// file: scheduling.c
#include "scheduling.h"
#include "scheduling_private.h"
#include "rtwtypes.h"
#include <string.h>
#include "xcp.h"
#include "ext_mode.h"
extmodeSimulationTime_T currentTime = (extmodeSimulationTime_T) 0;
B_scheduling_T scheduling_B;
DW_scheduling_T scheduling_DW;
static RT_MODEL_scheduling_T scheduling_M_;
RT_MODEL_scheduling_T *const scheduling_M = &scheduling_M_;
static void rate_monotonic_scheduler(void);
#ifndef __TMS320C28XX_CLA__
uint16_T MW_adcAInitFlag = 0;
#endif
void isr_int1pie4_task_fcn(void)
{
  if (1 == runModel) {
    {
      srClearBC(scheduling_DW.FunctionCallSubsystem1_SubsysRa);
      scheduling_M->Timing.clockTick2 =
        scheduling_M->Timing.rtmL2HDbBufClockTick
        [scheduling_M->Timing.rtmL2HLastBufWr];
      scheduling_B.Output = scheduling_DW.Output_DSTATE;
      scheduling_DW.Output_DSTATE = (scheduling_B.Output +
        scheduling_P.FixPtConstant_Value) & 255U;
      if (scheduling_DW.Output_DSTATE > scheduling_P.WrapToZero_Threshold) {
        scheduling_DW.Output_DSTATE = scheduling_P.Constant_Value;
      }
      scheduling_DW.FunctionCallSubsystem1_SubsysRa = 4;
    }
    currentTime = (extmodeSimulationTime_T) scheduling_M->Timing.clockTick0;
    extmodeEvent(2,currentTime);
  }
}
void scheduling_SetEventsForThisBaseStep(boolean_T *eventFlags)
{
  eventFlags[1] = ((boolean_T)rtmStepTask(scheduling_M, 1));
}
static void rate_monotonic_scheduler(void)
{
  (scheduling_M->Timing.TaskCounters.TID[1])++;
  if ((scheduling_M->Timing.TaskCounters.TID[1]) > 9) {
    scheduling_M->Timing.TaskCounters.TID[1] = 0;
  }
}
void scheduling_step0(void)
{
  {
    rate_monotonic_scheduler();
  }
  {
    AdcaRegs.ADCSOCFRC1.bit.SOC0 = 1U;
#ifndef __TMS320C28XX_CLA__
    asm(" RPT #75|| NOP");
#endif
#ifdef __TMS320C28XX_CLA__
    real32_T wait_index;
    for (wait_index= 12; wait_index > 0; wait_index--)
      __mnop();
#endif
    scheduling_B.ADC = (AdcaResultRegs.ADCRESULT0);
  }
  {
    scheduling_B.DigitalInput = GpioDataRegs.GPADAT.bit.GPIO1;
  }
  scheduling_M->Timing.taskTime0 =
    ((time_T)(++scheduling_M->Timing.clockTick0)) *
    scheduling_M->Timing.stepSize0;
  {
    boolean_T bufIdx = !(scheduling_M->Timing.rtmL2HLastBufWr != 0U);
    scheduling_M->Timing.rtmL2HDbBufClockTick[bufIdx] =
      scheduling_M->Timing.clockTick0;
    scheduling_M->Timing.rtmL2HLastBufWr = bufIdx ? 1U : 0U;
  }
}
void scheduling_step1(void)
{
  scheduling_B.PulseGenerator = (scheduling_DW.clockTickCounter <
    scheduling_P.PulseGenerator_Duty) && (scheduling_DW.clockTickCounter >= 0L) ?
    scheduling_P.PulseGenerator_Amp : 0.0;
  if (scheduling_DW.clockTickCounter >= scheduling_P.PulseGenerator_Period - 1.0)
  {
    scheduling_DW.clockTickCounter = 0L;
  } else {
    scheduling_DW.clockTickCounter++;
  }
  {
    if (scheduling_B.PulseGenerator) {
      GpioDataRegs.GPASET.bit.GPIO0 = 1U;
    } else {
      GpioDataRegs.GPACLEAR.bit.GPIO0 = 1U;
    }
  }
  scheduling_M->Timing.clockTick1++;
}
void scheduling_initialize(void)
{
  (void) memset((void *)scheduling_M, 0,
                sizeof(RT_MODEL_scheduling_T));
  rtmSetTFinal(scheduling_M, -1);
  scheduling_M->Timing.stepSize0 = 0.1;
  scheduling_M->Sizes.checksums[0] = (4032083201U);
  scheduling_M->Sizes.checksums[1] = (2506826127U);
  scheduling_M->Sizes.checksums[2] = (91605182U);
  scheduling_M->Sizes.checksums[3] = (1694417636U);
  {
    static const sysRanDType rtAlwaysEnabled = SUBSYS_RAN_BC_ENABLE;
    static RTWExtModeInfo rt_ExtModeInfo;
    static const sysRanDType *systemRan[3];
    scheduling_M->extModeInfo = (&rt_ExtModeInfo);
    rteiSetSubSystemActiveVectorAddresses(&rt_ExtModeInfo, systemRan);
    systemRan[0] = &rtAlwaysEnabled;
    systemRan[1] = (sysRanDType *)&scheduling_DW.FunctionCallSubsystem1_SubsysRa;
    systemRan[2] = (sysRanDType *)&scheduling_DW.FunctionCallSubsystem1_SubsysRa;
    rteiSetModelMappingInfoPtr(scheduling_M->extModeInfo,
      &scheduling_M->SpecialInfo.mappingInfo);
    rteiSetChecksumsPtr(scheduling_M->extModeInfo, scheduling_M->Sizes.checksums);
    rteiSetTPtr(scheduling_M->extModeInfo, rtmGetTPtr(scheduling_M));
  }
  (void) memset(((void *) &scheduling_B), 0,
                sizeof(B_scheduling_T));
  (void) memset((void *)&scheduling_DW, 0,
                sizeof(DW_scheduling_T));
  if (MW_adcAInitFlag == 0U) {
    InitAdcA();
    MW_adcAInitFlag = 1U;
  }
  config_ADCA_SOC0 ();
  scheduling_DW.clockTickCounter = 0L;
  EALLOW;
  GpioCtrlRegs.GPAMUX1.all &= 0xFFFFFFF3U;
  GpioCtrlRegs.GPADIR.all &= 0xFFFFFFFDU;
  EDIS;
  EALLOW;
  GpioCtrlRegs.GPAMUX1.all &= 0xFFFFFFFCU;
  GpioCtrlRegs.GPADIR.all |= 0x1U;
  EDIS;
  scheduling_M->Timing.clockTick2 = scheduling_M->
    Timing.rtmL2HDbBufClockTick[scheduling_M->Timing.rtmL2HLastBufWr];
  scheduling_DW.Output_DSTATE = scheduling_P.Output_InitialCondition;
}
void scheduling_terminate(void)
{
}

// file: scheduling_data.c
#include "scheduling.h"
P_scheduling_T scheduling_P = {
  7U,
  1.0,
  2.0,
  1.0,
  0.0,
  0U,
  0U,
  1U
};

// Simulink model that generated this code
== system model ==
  FunctionCallSubsystem1 : Subsystem  <- Trigger: C28xHardwareInterrupt#1
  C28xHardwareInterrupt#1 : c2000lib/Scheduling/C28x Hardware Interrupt
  ADC : c2802xlib/ADC
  DigitalInput : c2837xDlib/Digital Input
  DigitalOutput#1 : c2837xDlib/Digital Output  <- 1: PulseGenerator
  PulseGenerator : DiscretePulseGenerator  PulseWidth=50
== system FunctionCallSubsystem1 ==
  TriggerPort#1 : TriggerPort  TriggerType=function-call
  CounterLimited#1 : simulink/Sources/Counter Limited  uplimit=7
